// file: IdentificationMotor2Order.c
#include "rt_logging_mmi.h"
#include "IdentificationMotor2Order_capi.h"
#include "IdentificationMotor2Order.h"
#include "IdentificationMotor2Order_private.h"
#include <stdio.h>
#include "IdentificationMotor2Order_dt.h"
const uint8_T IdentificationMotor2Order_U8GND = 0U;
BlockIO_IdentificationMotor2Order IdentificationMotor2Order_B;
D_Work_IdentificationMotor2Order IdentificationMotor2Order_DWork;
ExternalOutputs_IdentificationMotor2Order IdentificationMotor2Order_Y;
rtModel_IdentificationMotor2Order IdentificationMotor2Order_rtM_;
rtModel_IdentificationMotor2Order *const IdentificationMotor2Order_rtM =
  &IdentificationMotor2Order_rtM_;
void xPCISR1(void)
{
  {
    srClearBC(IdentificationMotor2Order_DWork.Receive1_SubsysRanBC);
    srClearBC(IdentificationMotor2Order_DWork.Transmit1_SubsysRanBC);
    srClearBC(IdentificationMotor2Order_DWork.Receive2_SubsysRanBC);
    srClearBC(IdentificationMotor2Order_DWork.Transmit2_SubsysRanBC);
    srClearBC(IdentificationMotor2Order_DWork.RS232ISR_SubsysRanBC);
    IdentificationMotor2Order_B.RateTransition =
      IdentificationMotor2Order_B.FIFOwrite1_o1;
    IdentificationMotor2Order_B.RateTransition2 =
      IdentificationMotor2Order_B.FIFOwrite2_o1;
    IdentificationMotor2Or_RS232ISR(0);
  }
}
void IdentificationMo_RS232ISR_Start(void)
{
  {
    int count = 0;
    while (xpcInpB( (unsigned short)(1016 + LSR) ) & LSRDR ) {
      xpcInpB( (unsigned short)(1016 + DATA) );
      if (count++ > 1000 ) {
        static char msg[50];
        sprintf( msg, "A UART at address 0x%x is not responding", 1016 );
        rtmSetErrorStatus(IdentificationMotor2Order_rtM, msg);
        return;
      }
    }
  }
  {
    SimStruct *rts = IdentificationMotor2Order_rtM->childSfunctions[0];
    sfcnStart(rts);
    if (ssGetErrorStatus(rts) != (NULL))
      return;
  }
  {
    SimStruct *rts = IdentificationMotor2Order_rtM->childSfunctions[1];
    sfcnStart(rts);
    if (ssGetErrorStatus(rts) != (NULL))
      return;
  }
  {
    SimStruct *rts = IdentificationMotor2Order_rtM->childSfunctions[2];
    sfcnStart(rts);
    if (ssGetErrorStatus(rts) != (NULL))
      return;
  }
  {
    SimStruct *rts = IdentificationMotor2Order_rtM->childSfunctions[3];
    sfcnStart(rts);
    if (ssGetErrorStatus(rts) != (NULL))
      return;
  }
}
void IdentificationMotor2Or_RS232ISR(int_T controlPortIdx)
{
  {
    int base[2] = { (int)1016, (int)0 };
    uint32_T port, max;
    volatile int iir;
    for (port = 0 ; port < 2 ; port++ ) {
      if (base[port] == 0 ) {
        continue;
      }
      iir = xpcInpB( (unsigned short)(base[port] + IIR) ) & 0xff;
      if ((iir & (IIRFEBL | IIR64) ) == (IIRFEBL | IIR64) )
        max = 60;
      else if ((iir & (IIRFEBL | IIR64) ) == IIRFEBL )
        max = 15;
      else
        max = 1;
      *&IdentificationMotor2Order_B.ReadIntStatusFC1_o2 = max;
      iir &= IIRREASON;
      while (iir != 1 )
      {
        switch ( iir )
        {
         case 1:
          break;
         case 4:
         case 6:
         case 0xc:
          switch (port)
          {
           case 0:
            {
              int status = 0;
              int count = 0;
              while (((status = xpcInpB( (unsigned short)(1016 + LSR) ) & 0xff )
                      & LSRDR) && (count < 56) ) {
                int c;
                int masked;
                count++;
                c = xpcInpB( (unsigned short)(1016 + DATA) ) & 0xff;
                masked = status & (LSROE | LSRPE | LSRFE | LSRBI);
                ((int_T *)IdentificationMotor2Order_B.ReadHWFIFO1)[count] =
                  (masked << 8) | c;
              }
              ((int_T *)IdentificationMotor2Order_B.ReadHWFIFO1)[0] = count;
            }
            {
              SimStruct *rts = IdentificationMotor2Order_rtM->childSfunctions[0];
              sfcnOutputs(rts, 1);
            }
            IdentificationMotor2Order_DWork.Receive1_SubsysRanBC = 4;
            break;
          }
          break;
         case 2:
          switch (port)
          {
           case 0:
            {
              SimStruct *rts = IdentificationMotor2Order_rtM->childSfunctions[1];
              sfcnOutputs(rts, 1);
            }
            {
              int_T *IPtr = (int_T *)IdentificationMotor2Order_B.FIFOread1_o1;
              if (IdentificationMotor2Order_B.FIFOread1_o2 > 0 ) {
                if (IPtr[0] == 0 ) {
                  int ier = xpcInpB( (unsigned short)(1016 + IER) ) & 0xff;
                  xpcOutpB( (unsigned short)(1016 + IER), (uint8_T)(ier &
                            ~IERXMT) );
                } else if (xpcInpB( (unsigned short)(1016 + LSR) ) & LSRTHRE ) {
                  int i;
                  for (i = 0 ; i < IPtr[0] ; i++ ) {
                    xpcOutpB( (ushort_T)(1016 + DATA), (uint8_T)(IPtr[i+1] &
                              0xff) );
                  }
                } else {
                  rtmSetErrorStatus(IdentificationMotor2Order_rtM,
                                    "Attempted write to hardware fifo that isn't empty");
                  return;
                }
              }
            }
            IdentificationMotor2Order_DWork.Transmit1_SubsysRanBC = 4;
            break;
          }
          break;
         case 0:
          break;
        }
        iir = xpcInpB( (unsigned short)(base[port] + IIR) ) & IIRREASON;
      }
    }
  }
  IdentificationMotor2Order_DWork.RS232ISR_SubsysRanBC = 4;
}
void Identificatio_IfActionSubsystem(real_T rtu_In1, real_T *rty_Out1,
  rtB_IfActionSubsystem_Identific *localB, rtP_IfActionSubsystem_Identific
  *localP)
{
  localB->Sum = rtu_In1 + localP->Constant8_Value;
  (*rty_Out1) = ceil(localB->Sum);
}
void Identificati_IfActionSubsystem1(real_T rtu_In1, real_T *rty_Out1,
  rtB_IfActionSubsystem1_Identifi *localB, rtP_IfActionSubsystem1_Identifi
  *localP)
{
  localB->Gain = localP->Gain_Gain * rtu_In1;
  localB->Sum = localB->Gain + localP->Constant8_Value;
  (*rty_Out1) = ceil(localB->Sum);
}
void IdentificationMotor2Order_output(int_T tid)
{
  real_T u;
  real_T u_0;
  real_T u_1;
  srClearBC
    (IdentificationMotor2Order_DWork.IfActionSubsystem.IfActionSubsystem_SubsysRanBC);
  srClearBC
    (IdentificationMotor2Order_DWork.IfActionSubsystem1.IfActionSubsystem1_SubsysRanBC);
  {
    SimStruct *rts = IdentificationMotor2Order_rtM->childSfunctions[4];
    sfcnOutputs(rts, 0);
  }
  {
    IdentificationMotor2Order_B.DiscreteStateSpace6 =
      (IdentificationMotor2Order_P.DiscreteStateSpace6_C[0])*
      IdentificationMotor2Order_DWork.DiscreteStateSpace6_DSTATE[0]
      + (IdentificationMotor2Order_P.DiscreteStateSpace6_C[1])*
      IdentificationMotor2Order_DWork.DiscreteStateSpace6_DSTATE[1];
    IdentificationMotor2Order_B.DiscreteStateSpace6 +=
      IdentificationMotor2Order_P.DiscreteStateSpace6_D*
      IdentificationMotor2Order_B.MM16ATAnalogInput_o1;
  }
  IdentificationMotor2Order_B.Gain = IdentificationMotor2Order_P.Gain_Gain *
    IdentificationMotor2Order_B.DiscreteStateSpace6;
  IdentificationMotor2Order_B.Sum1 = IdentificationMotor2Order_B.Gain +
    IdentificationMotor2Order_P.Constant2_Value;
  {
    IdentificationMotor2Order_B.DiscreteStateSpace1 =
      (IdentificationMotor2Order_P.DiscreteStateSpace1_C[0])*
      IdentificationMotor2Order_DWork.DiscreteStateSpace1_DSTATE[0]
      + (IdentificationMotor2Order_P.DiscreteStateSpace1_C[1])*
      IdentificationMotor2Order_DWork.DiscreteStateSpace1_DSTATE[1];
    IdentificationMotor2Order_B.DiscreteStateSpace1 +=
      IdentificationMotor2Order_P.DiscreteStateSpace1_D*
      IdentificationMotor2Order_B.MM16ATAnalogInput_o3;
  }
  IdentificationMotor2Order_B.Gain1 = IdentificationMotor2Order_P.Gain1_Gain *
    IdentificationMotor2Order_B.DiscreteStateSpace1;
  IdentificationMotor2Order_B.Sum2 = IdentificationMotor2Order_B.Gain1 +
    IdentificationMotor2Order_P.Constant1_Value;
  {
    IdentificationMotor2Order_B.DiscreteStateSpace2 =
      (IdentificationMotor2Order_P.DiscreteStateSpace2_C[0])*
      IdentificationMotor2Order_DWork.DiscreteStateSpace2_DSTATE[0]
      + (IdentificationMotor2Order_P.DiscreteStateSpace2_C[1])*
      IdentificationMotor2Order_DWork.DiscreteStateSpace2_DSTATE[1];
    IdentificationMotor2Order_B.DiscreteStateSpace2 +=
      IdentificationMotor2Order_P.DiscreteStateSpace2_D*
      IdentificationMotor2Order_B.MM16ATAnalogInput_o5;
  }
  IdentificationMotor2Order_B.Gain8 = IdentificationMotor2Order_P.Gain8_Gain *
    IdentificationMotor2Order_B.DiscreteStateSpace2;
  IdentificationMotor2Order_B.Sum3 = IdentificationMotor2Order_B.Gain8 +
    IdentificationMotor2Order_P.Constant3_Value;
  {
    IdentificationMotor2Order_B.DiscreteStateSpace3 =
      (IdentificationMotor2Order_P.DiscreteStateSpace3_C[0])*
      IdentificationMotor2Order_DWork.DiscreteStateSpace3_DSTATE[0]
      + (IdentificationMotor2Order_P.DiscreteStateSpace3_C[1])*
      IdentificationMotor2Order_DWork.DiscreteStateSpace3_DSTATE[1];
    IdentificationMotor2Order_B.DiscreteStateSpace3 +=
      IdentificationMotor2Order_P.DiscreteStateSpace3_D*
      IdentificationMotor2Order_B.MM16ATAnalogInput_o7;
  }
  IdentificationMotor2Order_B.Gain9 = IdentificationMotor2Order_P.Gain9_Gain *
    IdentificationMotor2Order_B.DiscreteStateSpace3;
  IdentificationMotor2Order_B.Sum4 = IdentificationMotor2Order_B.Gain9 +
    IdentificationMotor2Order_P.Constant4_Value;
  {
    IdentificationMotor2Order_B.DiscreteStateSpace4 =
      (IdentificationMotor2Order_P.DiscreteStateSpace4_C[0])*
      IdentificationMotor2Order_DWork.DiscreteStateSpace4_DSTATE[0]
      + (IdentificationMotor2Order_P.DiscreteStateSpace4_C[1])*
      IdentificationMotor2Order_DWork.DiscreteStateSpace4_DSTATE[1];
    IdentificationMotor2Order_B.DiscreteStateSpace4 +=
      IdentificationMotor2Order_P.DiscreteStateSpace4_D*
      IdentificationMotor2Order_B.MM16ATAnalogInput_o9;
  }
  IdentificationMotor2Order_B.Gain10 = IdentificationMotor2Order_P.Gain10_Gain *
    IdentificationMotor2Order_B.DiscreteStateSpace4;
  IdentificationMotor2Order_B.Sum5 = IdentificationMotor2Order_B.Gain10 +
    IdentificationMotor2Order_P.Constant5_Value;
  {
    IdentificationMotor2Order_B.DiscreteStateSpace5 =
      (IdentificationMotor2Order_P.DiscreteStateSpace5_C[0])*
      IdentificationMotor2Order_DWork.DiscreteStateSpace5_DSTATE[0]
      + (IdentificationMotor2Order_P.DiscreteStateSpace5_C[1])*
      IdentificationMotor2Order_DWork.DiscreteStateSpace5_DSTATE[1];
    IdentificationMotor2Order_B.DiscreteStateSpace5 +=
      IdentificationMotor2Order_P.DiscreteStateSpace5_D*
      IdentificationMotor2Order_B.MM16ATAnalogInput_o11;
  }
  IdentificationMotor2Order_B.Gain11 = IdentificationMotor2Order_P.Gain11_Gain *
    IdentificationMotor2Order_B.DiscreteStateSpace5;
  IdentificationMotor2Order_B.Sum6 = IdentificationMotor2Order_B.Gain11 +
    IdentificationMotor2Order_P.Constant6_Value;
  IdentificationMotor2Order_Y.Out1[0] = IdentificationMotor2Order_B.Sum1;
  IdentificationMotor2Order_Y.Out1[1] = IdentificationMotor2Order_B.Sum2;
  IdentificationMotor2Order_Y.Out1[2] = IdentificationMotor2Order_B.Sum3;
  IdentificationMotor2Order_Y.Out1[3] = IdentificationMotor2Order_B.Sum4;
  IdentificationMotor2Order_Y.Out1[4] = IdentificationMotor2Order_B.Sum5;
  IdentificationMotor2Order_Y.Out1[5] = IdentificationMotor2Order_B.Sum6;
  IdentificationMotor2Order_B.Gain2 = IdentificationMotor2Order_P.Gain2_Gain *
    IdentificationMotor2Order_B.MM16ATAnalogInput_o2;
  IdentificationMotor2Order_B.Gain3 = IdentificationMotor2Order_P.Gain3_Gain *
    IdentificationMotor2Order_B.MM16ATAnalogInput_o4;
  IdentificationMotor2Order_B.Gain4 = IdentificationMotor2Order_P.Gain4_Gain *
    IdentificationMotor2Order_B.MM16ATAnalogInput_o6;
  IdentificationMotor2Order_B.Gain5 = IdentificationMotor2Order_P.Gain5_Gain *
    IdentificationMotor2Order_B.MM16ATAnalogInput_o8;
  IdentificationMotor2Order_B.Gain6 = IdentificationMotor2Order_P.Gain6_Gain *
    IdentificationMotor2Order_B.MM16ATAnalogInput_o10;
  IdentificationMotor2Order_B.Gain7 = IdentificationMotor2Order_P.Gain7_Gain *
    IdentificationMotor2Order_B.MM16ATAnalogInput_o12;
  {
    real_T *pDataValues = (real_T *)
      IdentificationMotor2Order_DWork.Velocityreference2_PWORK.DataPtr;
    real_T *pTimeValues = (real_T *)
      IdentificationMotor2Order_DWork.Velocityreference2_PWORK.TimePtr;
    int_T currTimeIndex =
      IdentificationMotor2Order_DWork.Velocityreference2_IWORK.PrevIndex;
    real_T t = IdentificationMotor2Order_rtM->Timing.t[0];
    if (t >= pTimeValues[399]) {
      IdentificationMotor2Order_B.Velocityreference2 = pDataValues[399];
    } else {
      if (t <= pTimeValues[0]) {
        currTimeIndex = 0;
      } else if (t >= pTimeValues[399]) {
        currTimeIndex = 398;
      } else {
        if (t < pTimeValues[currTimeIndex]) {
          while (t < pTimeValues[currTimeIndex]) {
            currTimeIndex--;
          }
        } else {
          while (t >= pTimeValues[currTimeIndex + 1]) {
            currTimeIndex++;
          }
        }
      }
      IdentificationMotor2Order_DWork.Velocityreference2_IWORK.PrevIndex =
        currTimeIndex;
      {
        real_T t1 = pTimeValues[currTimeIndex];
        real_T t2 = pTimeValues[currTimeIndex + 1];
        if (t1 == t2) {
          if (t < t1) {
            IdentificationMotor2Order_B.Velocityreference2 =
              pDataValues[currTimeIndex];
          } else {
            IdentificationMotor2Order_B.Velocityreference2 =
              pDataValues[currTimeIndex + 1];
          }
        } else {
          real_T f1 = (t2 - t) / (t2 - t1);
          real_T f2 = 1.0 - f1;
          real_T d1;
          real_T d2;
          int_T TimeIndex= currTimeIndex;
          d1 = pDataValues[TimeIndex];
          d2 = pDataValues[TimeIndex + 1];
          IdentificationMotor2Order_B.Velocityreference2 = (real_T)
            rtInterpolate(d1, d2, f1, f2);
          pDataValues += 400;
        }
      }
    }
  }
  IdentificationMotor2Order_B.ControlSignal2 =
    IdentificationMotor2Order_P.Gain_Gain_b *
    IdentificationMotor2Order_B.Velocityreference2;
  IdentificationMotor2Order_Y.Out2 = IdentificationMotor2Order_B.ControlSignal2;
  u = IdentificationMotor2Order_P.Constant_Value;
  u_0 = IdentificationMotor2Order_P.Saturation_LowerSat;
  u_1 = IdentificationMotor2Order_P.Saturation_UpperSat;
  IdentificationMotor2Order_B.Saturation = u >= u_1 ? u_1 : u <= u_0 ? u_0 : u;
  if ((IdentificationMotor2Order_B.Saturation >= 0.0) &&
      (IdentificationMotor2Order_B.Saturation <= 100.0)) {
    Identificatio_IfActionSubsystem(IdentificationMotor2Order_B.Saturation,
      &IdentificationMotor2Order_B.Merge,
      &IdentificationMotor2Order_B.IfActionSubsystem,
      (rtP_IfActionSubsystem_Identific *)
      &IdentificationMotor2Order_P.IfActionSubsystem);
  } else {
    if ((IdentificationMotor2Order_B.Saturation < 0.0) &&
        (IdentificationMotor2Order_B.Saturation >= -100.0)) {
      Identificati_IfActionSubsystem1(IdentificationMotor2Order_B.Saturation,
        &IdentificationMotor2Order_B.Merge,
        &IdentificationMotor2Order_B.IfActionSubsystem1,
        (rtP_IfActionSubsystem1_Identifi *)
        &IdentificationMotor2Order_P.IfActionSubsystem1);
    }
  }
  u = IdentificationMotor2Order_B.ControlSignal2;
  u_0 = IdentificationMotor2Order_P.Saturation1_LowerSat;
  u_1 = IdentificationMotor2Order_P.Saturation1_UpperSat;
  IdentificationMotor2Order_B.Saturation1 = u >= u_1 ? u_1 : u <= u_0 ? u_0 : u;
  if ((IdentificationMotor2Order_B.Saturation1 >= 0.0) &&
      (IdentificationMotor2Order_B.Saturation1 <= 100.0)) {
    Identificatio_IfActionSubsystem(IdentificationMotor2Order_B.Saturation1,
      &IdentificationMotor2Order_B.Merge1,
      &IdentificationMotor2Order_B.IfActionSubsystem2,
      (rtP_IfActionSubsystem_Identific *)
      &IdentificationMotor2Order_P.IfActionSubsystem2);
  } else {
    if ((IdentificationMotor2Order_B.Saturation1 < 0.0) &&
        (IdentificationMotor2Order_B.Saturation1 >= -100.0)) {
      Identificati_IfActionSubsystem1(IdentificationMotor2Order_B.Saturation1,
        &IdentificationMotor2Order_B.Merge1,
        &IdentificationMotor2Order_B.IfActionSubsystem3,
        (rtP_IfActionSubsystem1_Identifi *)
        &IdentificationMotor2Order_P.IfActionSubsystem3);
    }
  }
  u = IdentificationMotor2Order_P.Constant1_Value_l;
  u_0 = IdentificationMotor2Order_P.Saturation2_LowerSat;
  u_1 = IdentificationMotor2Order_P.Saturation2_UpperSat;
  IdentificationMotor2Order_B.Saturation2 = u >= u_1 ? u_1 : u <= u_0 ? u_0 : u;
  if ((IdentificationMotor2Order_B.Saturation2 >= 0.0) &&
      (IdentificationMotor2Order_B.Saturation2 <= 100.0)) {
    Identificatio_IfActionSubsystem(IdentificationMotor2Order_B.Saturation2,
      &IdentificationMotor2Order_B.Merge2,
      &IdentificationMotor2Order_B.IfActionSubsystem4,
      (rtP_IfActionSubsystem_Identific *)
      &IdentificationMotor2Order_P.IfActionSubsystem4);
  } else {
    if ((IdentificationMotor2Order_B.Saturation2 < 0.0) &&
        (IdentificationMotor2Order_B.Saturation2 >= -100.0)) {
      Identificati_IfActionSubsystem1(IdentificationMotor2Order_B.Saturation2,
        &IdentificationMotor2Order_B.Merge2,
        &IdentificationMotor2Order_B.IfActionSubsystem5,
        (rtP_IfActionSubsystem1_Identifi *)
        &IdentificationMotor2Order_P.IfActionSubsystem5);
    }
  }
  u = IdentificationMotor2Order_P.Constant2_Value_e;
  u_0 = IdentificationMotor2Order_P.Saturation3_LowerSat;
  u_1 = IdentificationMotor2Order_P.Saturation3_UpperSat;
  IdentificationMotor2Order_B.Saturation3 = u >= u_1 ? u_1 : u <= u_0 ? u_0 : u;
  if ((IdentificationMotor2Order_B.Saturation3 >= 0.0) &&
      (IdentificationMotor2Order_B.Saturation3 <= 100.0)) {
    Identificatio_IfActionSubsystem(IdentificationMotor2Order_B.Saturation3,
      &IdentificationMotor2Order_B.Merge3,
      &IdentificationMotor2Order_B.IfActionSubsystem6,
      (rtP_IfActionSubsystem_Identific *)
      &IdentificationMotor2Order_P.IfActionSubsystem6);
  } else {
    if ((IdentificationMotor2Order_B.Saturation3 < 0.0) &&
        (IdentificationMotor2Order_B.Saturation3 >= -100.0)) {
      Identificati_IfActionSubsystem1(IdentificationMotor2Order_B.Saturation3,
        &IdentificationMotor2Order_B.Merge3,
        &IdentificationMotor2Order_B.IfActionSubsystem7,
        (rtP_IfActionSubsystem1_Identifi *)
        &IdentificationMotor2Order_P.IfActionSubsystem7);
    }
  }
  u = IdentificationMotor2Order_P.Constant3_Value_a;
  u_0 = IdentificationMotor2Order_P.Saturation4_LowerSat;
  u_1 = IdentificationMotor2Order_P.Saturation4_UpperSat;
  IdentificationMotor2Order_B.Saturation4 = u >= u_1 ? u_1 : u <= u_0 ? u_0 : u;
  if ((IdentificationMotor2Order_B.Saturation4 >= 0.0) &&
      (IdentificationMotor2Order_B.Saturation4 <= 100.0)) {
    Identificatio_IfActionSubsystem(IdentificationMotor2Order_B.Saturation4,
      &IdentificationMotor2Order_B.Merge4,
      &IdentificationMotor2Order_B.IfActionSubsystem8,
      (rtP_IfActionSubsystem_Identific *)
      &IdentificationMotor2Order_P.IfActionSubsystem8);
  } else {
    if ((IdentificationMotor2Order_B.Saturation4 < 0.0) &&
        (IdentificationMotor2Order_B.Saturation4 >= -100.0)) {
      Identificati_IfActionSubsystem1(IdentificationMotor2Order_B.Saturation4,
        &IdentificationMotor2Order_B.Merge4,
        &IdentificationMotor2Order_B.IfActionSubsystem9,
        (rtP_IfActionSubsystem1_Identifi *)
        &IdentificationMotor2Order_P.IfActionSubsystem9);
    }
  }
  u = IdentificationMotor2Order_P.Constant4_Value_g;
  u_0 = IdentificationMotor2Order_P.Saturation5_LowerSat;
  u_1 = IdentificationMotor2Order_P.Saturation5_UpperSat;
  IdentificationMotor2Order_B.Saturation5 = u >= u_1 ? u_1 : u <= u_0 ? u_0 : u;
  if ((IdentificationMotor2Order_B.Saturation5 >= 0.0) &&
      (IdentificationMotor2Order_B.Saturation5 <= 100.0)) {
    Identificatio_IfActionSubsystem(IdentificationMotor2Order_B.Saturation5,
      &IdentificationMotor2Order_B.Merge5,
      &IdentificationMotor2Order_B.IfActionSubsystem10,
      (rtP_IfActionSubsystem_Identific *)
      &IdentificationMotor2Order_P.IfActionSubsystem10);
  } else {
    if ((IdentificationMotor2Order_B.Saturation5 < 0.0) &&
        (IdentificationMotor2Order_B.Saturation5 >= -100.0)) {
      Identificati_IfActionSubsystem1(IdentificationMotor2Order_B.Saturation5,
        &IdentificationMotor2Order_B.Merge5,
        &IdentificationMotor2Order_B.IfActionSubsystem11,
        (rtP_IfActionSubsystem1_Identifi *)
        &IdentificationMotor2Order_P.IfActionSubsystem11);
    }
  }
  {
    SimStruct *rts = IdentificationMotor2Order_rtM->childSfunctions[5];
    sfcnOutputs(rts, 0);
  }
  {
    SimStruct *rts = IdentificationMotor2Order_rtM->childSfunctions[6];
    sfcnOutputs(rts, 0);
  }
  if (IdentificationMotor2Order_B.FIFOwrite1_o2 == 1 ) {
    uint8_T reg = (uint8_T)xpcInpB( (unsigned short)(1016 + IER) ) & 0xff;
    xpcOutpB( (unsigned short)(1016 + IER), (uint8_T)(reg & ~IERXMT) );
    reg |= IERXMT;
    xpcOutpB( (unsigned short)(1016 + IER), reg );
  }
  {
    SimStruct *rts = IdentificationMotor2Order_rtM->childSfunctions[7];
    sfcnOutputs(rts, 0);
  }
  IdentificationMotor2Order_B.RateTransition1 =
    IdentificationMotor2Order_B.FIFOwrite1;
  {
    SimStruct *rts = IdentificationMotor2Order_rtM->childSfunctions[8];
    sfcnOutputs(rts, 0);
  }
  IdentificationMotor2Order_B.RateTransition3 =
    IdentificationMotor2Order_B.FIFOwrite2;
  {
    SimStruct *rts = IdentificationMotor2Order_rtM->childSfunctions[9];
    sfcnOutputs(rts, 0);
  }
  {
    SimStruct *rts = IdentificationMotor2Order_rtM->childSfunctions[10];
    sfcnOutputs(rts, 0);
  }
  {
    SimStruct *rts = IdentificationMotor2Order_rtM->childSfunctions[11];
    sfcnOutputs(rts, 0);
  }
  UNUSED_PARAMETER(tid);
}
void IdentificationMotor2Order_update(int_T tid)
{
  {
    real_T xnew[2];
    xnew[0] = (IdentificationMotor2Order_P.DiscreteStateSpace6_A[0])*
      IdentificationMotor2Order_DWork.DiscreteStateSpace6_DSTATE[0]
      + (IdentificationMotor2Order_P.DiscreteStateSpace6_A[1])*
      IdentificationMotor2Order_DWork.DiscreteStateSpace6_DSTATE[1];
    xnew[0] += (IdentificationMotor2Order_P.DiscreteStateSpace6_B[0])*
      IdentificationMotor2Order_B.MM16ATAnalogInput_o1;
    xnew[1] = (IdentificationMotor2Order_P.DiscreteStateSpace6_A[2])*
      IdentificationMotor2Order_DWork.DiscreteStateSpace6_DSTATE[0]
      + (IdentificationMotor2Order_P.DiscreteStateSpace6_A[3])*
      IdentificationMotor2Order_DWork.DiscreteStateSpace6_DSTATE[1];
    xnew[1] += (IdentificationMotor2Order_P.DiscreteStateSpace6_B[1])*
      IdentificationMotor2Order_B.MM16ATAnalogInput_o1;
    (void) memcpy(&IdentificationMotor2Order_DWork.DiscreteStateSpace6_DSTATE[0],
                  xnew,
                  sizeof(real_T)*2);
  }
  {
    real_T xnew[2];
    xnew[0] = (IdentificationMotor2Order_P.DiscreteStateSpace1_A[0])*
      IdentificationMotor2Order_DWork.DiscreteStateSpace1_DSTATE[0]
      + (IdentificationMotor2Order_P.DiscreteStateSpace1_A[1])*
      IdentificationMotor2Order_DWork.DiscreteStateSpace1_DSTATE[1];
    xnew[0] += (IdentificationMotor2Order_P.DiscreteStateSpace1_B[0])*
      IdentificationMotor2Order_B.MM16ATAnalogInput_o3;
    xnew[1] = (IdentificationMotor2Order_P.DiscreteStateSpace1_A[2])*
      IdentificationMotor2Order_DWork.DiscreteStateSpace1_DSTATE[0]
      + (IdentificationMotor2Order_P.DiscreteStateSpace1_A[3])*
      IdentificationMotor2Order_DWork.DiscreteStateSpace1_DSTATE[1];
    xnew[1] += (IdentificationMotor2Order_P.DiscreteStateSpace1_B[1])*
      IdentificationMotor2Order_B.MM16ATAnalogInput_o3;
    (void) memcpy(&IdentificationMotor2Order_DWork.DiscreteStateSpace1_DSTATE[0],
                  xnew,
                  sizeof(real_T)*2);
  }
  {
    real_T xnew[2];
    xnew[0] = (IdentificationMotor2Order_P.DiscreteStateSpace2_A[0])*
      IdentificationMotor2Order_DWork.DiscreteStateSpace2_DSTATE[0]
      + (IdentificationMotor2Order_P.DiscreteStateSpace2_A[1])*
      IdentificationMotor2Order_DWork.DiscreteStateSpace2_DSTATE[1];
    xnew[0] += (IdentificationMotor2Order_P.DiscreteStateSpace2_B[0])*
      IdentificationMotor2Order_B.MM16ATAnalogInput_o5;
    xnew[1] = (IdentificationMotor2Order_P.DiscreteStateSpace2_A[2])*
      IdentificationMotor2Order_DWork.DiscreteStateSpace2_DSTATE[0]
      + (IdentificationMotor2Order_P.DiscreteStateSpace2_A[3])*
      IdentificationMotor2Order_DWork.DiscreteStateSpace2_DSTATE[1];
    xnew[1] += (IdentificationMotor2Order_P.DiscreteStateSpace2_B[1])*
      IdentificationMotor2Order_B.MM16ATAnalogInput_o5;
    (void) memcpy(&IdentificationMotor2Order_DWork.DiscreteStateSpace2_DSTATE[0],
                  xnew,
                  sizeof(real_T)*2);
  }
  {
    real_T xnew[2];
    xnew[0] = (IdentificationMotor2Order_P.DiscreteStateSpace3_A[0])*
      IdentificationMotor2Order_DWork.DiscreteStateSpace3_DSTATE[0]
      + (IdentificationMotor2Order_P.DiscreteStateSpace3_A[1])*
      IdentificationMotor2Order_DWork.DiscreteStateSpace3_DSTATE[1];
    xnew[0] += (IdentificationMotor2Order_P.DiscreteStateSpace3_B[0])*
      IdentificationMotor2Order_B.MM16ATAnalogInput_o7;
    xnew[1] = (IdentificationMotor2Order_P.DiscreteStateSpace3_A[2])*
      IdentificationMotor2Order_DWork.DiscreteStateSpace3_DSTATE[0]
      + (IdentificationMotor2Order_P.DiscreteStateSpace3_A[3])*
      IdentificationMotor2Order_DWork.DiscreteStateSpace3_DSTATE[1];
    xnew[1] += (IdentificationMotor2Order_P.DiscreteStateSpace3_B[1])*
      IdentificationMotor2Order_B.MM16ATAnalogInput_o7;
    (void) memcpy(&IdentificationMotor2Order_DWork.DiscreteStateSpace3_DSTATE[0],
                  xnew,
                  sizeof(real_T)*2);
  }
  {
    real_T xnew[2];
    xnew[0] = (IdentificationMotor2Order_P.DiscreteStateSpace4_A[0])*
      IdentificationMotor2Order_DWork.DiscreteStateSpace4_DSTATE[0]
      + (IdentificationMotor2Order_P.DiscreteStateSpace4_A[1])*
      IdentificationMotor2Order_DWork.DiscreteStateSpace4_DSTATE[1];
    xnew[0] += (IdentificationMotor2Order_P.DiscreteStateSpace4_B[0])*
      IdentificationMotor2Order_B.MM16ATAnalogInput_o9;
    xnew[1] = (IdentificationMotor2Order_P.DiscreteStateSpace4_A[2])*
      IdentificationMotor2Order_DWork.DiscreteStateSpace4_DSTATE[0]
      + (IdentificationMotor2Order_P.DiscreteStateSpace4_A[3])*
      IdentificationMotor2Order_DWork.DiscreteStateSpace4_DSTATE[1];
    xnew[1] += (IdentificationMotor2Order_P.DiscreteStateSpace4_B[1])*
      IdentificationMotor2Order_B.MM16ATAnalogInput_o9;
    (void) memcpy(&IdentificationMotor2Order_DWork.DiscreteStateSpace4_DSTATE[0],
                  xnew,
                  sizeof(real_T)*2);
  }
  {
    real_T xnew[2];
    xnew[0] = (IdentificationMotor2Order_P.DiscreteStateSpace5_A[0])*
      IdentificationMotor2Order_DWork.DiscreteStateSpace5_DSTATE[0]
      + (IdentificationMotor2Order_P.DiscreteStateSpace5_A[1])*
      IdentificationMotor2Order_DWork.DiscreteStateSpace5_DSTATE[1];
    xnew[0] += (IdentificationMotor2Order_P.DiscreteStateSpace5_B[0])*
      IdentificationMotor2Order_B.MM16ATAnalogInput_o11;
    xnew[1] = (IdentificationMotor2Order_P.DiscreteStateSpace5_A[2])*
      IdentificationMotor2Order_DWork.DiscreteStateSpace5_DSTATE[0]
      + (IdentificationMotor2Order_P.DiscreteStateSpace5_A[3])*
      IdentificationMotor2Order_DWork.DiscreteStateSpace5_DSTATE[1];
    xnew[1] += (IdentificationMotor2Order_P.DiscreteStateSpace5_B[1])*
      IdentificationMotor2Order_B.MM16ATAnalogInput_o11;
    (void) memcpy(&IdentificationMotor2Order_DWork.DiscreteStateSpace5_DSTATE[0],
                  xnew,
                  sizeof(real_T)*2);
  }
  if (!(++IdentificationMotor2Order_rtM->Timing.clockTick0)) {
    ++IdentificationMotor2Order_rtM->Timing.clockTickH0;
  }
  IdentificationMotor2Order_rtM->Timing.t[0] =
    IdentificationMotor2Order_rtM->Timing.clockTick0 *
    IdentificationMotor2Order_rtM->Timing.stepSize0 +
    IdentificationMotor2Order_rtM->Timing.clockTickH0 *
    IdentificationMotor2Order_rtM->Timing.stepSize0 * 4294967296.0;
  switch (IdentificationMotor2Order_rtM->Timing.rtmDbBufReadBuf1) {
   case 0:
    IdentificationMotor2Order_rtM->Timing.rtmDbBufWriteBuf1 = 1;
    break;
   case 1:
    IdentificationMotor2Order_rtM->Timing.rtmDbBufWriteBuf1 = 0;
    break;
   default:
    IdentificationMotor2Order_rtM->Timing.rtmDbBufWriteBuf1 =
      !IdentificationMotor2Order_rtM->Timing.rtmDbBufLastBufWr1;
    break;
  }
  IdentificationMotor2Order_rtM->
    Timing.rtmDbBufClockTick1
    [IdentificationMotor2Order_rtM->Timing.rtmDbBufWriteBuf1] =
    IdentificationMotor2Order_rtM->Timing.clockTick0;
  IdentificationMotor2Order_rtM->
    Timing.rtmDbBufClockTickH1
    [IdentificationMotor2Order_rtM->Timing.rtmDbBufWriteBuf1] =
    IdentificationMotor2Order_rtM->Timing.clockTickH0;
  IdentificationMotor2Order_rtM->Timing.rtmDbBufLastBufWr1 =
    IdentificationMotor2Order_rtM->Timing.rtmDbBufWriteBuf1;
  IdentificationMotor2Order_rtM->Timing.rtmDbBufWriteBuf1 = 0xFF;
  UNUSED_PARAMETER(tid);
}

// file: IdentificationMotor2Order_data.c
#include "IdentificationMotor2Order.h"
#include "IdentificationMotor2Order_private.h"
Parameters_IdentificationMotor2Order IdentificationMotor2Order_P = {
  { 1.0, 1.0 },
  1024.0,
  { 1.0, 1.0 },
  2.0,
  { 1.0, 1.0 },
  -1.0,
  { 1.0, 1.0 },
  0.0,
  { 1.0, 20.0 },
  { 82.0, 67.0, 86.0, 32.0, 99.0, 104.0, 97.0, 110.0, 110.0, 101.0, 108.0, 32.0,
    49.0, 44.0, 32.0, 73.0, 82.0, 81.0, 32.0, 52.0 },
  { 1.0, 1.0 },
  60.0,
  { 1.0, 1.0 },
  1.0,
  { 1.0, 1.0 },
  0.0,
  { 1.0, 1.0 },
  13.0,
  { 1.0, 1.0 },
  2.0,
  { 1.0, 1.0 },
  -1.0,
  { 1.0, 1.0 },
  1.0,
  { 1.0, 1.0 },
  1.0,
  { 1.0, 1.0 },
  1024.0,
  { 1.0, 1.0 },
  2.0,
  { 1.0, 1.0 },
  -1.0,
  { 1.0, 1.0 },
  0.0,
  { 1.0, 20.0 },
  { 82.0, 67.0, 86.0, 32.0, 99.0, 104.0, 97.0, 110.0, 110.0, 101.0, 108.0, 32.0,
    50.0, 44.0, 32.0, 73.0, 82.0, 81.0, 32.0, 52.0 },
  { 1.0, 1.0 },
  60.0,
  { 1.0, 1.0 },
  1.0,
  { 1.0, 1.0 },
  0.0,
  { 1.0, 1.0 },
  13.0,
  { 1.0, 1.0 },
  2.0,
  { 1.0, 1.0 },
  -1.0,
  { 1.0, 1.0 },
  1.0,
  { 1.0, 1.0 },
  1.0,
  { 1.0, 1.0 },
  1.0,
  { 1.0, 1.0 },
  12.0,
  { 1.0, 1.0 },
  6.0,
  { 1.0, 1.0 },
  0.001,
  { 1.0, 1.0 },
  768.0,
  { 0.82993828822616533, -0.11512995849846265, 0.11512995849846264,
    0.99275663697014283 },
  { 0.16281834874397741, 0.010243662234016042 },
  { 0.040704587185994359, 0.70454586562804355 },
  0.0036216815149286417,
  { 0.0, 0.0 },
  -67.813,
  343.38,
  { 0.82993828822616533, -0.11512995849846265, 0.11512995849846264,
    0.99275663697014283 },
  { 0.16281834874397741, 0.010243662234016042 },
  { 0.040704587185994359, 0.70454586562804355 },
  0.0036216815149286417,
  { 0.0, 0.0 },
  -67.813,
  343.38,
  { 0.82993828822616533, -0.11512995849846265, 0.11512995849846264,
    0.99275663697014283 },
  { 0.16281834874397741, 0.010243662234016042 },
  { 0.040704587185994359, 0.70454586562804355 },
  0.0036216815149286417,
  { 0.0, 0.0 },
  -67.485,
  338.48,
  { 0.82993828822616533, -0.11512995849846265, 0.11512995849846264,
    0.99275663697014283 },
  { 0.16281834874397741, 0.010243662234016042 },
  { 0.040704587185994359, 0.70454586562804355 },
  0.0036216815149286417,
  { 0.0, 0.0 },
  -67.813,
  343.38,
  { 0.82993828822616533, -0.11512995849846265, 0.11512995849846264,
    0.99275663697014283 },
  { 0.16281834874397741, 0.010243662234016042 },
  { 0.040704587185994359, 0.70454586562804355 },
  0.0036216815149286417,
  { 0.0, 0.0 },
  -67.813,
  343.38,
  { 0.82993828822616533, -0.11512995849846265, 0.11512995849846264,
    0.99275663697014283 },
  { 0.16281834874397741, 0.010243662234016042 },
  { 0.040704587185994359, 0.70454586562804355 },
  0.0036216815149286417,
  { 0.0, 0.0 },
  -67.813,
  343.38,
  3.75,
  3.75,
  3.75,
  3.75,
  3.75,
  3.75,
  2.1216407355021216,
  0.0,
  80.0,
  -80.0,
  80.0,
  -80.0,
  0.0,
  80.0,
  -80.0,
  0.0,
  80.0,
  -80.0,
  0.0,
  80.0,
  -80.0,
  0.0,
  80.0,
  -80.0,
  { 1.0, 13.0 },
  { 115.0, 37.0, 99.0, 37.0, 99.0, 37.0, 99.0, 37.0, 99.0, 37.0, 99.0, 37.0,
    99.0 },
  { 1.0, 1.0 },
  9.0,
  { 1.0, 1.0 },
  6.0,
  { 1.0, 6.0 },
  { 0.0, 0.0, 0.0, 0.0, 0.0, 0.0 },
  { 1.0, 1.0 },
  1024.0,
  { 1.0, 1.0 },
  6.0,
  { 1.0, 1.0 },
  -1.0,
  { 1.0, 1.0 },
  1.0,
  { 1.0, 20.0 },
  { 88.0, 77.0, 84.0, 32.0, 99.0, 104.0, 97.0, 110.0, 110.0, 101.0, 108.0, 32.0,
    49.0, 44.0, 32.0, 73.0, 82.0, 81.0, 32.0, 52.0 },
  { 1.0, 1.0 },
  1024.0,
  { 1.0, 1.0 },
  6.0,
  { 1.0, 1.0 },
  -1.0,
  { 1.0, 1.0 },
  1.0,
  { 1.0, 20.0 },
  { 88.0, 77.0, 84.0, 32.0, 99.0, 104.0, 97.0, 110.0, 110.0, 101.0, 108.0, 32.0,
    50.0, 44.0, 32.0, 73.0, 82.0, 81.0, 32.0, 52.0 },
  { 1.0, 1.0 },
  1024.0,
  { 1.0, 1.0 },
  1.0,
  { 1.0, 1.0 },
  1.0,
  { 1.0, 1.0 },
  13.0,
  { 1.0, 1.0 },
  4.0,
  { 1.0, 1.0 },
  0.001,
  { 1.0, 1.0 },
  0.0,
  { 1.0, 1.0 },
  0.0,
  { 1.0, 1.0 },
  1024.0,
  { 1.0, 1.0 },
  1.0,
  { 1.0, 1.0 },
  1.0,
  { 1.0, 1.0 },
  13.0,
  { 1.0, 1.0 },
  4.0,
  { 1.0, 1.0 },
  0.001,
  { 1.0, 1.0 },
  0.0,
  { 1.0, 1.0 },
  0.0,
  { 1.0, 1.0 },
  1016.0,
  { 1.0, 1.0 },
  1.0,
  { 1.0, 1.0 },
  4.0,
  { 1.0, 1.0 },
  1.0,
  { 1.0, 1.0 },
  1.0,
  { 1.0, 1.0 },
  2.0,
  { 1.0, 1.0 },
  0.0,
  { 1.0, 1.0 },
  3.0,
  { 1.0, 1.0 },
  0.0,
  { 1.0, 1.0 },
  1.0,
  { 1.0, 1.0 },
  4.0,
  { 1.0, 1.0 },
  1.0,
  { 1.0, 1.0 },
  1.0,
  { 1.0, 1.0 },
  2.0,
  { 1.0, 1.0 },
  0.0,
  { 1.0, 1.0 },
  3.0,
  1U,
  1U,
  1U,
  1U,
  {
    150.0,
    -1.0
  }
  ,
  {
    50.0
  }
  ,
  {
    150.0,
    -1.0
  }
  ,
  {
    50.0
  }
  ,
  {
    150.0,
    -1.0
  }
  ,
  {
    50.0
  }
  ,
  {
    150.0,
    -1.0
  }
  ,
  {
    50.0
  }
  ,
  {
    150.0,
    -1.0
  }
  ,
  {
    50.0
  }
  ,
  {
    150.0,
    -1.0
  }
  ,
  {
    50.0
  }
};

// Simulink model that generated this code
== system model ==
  Out1 : Outport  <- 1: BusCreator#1
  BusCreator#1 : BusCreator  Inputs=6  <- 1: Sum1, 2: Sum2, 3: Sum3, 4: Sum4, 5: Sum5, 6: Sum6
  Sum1 : Sum  Inputs=++  <- 1: Gain, 2: Constant2
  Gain : Gain  Gain=-67.813  <- 1: DiscreteStateSpace6
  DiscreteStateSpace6 : DiscreteStateSpace  A=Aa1  B=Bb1  C=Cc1  D=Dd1  X0=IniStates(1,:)  <- 1: MM16ATAnalogInput
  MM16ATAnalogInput : Diamond16AT_UNAL/Diamond MM-16-AT/MM-16-AT Analog Input
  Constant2 : Constant  Value=343.38
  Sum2 : Sum  Inputs=++  <- 1: Gain1, 2: Constant1
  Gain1 : Gain  Gain=-67.813  <- 1: DiscreteStateSpace1
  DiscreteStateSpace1 : DiscreteStateSpace  A=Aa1  B=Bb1  C=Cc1  D=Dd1  X0=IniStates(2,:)  <- 1: MM16ATAnalogInput/3
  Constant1 : Constant  Value=343.38
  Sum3 : Sum  Inputs=++  <- 1: Gain8, 2: Constant3
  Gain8 : Gain  Gain=-67.485  <- 1: DiscreteStateSpace2
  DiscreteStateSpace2 : DiscreteStateSpace  A=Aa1  B=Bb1  C=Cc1  D=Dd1  X0=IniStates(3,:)  <- 1: MM16ATAnalogInput/5
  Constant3 : Constant  Value=338.48
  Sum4 : Sum  Inputs=++  <- 1: Gain9, 2: Constant4
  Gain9 : Gain  Gain=-67.813  <- 1: DiscreteStateSpace3
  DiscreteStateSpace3 : DiscreteStateSpace  A=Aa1  B=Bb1  C=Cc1  D=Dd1  X0=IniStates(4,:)  <- 1: MM16ATAnalogInput/7
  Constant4 : Constant  Value=343.38
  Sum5 : Sum  Inputs=++  <- 1: Gain10, 2: Constant5
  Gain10 : Gain  Gain=-67.813  <- 1: DiscreteStateSpace4
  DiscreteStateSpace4 : DiscreteStateSpace  A=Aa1  B=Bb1  C=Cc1  D=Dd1  X0=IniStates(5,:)  <- 1: MM16ATAnalogInput/9
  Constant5 : Constant  Value=343.38
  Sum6 : Sum  Inputs=++  <- 1: Gain11, 2: Constant6
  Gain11 : Gain  Gain=-67.813  <- 1: DiscreteStateSpace5
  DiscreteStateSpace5 : DiscreteStateSpace  A=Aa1  B=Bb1  C=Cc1  D=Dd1  X0=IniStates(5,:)  <- 1: MM16ATAnalogInput/11
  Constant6 : Constant  Value=343.38
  Out2 : Outport  <- 1: Gain#1
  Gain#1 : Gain  Gain=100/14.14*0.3  <- 1: Velocityreference2
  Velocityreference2 : FromWorkspace
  Gain2 : Gain  Gain=3.75  <- 1: MM16ATAnalogInput/2
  Gain3 : Gain  Gain=3.75  <- 1: MM16ATAnalogInput/4
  Gain4 : Gain  Gain=3.75  <- 1: MM16ATAnalogInput/6
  Gain5 : Gain  Gain=3.75  <- 1: MM16ATAnalogInput/8
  Gain6 : Gain  Gain=3.75  <- 1: MM16ATAnalogInput/10
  Gain7 : Gain  Gain=3.75  <- 1: MM16ATAnalogInput/12
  MotorsF4STMPWM#1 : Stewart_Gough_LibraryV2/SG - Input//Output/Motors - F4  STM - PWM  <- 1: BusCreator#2
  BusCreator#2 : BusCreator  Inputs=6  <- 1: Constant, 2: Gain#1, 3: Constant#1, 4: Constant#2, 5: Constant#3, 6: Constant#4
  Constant : Constant  Value=0
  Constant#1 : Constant  Value=0
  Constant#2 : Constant  Value=0
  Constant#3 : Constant  Value=0
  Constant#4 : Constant  Value=0
